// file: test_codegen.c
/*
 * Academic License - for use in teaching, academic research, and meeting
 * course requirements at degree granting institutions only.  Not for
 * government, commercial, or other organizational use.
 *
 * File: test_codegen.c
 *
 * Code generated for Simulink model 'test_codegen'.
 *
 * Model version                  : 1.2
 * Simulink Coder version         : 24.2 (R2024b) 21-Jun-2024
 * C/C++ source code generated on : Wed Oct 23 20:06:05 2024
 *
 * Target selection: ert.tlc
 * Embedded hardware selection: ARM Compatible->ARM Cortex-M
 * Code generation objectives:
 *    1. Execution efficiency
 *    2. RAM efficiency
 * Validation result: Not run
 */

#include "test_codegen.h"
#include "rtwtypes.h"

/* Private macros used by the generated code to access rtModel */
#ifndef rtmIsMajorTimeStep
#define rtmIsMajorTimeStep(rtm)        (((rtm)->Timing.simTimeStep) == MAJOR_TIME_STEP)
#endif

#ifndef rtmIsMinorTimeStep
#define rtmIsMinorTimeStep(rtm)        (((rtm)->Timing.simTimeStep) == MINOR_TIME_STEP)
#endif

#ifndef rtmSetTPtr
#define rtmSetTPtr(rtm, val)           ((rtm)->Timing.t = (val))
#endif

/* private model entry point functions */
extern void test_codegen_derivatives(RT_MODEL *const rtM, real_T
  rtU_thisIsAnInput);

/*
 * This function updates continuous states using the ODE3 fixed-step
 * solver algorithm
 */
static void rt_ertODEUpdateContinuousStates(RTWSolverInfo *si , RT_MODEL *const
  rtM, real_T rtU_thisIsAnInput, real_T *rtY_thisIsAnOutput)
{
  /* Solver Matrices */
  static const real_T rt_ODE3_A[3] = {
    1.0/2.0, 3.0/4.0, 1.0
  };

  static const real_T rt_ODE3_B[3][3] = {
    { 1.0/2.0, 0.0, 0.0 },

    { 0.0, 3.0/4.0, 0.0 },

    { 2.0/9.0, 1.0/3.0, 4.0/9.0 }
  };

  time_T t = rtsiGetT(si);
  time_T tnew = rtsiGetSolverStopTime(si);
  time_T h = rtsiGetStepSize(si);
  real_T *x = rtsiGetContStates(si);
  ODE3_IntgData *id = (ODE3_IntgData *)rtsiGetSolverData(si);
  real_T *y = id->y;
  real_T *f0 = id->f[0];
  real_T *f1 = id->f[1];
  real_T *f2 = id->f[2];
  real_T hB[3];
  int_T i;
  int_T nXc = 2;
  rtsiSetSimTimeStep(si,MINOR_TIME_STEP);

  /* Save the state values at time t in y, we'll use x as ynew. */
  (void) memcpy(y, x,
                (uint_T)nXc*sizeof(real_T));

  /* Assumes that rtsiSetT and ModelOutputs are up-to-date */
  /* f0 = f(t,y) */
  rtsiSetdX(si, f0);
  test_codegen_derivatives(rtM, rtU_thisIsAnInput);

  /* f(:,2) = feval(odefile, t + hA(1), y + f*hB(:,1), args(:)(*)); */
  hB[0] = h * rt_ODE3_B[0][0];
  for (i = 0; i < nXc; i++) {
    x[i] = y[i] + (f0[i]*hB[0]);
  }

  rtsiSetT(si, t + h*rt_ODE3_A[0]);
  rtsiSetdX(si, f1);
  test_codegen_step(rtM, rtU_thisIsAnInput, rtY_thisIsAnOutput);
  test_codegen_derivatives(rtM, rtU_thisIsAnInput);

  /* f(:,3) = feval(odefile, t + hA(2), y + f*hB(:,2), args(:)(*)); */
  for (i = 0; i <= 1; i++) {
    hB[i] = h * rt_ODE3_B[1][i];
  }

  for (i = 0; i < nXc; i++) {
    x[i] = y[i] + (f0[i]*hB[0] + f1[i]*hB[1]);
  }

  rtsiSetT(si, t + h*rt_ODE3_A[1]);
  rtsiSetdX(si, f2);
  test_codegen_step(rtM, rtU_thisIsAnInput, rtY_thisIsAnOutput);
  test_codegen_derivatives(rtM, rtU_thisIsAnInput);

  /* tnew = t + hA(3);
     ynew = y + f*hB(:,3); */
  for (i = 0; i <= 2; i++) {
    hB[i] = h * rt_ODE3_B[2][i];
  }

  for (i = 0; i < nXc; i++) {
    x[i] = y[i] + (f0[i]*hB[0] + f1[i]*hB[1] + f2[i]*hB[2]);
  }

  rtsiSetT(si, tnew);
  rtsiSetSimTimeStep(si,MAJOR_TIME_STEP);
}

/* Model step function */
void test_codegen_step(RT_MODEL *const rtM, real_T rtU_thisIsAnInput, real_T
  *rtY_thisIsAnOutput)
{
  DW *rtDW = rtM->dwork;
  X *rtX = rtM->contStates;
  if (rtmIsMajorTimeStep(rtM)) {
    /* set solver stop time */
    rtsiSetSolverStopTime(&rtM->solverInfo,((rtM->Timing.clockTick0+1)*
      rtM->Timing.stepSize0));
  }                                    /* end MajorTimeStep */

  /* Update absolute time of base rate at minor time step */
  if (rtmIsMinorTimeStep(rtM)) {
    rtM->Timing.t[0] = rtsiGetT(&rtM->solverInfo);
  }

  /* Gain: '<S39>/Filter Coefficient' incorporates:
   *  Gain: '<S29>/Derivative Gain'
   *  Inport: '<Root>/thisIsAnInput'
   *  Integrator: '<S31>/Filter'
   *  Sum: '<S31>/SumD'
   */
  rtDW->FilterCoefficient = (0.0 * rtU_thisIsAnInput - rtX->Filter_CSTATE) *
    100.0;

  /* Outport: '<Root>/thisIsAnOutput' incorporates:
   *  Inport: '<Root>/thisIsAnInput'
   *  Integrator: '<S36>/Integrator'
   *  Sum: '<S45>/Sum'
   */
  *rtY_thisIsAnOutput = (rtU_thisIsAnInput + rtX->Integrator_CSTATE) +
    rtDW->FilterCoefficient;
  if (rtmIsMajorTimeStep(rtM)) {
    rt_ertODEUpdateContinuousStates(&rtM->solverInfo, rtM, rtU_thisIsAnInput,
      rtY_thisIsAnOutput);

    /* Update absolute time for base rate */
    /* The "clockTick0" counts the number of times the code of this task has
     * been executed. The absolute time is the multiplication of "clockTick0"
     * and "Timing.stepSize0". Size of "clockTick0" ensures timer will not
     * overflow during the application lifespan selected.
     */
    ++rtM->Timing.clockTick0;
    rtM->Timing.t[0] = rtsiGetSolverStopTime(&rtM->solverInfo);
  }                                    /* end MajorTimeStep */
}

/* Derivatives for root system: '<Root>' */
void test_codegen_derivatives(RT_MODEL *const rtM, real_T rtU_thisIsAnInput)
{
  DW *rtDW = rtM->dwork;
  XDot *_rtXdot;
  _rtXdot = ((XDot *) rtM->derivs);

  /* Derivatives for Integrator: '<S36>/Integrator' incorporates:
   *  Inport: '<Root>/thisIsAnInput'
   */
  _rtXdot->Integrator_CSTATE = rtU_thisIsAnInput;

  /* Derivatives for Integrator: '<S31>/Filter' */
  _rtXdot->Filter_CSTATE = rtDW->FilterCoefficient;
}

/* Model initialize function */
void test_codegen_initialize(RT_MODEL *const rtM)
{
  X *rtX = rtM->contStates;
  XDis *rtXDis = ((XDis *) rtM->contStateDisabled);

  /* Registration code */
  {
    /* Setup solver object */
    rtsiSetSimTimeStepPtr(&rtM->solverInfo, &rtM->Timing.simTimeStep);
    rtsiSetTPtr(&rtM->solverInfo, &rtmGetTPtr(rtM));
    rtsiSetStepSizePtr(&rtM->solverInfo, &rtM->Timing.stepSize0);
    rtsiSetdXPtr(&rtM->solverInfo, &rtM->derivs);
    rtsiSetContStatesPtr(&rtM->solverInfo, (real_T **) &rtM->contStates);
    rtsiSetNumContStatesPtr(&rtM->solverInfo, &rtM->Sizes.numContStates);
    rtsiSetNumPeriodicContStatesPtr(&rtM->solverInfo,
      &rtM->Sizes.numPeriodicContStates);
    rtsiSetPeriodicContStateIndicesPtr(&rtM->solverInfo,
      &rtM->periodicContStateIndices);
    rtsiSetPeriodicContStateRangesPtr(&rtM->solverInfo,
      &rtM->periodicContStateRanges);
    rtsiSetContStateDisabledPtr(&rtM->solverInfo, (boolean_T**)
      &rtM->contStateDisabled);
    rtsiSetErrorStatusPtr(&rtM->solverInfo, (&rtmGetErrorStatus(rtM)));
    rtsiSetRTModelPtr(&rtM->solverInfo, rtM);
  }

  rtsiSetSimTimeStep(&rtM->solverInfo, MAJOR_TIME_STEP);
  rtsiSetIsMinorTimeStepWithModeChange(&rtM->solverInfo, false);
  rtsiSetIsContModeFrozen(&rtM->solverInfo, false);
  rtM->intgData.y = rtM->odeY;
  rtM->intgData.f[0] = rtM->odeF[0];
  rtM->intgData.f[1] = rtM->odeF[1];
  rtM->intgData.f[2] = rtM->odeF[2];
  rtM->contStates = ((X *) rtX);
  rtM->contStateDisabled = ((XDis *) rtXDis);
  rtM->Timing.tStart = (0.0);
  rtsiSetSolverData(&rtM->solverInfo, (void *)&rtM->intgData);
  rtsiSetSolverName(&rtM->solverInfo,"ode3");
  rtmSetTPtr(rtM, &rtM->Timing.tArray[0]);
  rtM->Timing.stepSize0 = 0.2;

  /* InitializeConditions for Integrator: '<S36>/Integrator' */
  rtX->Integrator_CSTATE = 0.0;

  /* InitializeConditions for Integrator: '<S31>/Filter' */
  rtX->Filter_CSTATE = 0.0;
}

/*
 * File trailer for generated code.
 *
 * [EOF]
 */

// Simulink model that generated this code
simulink model "test_codegen"  (R2024b)
settings: Solver=FixedStepAuto  StartTime=0.0  StopTime=10.0  RelTol=1e-3
undefined symbols (not defined in the file): P_test_variable
libraries: slpidlib x1

== system test_codegen ==
  thisIsAnInput : Inport
  PID Controller : slpidlib/PID Controller  Controller=PID  Form=Parallel  TimeDomain=Continuous-time  UseExternalTs=off  SampleTime=-1  IntegratorMethod=Forward Euler  FilterMethod=Forward Euler  ControllerParametersSource=internal  P=P_test_variable  I=1  UseKiTs=off  D=0  UseExternalDerivativeSource=off  N=100  UseFilter=on  TunerSelectOption=Transfer Function Based (PID Tuner App)  InitialConditionSource=internal  InitialConditionForIntegrator=0  InitialConditionForFilter=0  DifferentiatorICPrevScaledInput=0  ExternalReset=none  TrackingMode=off  Kt=1  LimitOutput=off  SatLimitsSource=internal  UpperSaturationLimit=inf  LowerSaturationLimit=-inf  LinearizeAsGain=on  AntiWindupMode=none  Kb=1  LimitIntegrator=off  UpperIntegratorSaturationLimit=inf  LowerIntegratorSaturationLimit=-inf  POutMin=[]  POutMax=[]  IOutMin=[]  IOutMax=[]  DOutMin=[]  DOutMax=[]  NOutMin=[]  NOutMax=[]  SumOutMin=[]  SumOutMax=[]  SaturationOutMin=[]  SaturationOutMax=[]  PParamMin=[]  PParamMax=[]  IParamMin=[]  IParamMax=[]  DParamMin=[]  DParamMax=[]  NParamMin=[]  NParamMax=[]  KbParamMin=[]  KbParamMax=[]  KtParamMin=[]  KtParamMax=[]  KbOutMin=[]  KbOutMax=[]  KtOutMin=[]  KtOutMax=[]  IntegratorOutMin=[]  IntegratorOutMax=[]  FilterOutMin=[]  FilterOutMax=[]  SumI1OutMin=[]  SumI1OutMax=[]  SumI2OutMin=[]  SumI2OutMax=[]  SumI3OutMin=[]  SumI3OutMax=[]  SumI4OutMin=[]  SumI4OutMax=[]  SumDOutMin=[]  SumDOutMax=[]  DifferentiatorOutMin=[]  DifferentiatorOutMax=[]  FilterDiffOutCoefMin=[]  FilterDiffOutCoefMax=[]  ReciprocalOutMin=[]  ReciprocalOutMax=[]  SumDenOutMin=[]  SumDenOutMax=[]  SumNumOutMin=[]  SumNumOutMax=[]  DivideOutMin=[]  DivideOutMax=[]  UdiffTsProdOutMin=[]  UdiffTsProdOutMax=[]  NTsProdOutMin=[]  NTsProdOutMax=[]  UintegralTsProdOutMin=[]  UintegralTsProdOutMax=[]  UngainTsProdOutMin=[]  UngainTsProdOutMax=[]  ClampingZeroOutDataTypeStr=Inherit: Inherit via back propagation  ClampingZeroOutMin=[]  ClampingZeroOutMax=[]  FilterDenConstantOutDataTypeStr=Inherit: Inherit via back propagation  FilterDenConstantOutMin=[]  FilterDenConstantOutMax=[]  PCopyOutDataTypeStr=Inherit: Inherit via back propagation  PCopyOutMin=[]  PCopyOutMax=[]  NCopyOutDataTypeStr=Inherit: Inherit via back propagation  NCopyOutMin=[]  NCopyOutMax=[]  IntegratorContinuousStateAttributes=''  IntegratorStateMustResolveToSignalObject=off  IntegratorRTWStateStorageClass=Auto  FilterContinuousStateAttributes=''  FilterStateMustResolveToSignalObject=off  FilterRTWStateStorageClass=Auto  ParallelPVariant=InternalParameters  IdealPVariant=Disabled  IVariant=InternalParameters  DVariant=InternalParameters  IntegratorVariant=Continuous  SatVariant=Disabled  AWVariant=Passthrough  PCopyVariant=Disabled  TRVariant=Disabled  FdbkBlocksVariant=Forward  IdealPFdbkVariant=Disabled  SatFdbkVariant=Disabled  DerivativeFilterVariant=ContFilter  NVariant=InternalParameters  NCopyVariant=Disabled  FilterICVariant=InternalICsFilter  IntegratorICVariant=InternalICs  ExternalResetVariant=Disabled  TRSumVariant=Passthrough  SumFdbkVariant=Disabled  SumVariant=Sum_PID  TsampFilterVariant=InternalTs  TsampNgainVariant=Passthrough  TsampIntegralVariant=Disabled_SignalSpec  ExternalSaturationOutDataTypeStr=Inherit: Same as second input  DerivativeSourceVariant=ErrorSignal  PreIntVariant=InternalPreInt
  thisIsAnOutput : Outport
  wires:
  thisIsAnInput/1 -> PID Controller/1
  PID Controller/1 -> thisIsAnOutput/1
